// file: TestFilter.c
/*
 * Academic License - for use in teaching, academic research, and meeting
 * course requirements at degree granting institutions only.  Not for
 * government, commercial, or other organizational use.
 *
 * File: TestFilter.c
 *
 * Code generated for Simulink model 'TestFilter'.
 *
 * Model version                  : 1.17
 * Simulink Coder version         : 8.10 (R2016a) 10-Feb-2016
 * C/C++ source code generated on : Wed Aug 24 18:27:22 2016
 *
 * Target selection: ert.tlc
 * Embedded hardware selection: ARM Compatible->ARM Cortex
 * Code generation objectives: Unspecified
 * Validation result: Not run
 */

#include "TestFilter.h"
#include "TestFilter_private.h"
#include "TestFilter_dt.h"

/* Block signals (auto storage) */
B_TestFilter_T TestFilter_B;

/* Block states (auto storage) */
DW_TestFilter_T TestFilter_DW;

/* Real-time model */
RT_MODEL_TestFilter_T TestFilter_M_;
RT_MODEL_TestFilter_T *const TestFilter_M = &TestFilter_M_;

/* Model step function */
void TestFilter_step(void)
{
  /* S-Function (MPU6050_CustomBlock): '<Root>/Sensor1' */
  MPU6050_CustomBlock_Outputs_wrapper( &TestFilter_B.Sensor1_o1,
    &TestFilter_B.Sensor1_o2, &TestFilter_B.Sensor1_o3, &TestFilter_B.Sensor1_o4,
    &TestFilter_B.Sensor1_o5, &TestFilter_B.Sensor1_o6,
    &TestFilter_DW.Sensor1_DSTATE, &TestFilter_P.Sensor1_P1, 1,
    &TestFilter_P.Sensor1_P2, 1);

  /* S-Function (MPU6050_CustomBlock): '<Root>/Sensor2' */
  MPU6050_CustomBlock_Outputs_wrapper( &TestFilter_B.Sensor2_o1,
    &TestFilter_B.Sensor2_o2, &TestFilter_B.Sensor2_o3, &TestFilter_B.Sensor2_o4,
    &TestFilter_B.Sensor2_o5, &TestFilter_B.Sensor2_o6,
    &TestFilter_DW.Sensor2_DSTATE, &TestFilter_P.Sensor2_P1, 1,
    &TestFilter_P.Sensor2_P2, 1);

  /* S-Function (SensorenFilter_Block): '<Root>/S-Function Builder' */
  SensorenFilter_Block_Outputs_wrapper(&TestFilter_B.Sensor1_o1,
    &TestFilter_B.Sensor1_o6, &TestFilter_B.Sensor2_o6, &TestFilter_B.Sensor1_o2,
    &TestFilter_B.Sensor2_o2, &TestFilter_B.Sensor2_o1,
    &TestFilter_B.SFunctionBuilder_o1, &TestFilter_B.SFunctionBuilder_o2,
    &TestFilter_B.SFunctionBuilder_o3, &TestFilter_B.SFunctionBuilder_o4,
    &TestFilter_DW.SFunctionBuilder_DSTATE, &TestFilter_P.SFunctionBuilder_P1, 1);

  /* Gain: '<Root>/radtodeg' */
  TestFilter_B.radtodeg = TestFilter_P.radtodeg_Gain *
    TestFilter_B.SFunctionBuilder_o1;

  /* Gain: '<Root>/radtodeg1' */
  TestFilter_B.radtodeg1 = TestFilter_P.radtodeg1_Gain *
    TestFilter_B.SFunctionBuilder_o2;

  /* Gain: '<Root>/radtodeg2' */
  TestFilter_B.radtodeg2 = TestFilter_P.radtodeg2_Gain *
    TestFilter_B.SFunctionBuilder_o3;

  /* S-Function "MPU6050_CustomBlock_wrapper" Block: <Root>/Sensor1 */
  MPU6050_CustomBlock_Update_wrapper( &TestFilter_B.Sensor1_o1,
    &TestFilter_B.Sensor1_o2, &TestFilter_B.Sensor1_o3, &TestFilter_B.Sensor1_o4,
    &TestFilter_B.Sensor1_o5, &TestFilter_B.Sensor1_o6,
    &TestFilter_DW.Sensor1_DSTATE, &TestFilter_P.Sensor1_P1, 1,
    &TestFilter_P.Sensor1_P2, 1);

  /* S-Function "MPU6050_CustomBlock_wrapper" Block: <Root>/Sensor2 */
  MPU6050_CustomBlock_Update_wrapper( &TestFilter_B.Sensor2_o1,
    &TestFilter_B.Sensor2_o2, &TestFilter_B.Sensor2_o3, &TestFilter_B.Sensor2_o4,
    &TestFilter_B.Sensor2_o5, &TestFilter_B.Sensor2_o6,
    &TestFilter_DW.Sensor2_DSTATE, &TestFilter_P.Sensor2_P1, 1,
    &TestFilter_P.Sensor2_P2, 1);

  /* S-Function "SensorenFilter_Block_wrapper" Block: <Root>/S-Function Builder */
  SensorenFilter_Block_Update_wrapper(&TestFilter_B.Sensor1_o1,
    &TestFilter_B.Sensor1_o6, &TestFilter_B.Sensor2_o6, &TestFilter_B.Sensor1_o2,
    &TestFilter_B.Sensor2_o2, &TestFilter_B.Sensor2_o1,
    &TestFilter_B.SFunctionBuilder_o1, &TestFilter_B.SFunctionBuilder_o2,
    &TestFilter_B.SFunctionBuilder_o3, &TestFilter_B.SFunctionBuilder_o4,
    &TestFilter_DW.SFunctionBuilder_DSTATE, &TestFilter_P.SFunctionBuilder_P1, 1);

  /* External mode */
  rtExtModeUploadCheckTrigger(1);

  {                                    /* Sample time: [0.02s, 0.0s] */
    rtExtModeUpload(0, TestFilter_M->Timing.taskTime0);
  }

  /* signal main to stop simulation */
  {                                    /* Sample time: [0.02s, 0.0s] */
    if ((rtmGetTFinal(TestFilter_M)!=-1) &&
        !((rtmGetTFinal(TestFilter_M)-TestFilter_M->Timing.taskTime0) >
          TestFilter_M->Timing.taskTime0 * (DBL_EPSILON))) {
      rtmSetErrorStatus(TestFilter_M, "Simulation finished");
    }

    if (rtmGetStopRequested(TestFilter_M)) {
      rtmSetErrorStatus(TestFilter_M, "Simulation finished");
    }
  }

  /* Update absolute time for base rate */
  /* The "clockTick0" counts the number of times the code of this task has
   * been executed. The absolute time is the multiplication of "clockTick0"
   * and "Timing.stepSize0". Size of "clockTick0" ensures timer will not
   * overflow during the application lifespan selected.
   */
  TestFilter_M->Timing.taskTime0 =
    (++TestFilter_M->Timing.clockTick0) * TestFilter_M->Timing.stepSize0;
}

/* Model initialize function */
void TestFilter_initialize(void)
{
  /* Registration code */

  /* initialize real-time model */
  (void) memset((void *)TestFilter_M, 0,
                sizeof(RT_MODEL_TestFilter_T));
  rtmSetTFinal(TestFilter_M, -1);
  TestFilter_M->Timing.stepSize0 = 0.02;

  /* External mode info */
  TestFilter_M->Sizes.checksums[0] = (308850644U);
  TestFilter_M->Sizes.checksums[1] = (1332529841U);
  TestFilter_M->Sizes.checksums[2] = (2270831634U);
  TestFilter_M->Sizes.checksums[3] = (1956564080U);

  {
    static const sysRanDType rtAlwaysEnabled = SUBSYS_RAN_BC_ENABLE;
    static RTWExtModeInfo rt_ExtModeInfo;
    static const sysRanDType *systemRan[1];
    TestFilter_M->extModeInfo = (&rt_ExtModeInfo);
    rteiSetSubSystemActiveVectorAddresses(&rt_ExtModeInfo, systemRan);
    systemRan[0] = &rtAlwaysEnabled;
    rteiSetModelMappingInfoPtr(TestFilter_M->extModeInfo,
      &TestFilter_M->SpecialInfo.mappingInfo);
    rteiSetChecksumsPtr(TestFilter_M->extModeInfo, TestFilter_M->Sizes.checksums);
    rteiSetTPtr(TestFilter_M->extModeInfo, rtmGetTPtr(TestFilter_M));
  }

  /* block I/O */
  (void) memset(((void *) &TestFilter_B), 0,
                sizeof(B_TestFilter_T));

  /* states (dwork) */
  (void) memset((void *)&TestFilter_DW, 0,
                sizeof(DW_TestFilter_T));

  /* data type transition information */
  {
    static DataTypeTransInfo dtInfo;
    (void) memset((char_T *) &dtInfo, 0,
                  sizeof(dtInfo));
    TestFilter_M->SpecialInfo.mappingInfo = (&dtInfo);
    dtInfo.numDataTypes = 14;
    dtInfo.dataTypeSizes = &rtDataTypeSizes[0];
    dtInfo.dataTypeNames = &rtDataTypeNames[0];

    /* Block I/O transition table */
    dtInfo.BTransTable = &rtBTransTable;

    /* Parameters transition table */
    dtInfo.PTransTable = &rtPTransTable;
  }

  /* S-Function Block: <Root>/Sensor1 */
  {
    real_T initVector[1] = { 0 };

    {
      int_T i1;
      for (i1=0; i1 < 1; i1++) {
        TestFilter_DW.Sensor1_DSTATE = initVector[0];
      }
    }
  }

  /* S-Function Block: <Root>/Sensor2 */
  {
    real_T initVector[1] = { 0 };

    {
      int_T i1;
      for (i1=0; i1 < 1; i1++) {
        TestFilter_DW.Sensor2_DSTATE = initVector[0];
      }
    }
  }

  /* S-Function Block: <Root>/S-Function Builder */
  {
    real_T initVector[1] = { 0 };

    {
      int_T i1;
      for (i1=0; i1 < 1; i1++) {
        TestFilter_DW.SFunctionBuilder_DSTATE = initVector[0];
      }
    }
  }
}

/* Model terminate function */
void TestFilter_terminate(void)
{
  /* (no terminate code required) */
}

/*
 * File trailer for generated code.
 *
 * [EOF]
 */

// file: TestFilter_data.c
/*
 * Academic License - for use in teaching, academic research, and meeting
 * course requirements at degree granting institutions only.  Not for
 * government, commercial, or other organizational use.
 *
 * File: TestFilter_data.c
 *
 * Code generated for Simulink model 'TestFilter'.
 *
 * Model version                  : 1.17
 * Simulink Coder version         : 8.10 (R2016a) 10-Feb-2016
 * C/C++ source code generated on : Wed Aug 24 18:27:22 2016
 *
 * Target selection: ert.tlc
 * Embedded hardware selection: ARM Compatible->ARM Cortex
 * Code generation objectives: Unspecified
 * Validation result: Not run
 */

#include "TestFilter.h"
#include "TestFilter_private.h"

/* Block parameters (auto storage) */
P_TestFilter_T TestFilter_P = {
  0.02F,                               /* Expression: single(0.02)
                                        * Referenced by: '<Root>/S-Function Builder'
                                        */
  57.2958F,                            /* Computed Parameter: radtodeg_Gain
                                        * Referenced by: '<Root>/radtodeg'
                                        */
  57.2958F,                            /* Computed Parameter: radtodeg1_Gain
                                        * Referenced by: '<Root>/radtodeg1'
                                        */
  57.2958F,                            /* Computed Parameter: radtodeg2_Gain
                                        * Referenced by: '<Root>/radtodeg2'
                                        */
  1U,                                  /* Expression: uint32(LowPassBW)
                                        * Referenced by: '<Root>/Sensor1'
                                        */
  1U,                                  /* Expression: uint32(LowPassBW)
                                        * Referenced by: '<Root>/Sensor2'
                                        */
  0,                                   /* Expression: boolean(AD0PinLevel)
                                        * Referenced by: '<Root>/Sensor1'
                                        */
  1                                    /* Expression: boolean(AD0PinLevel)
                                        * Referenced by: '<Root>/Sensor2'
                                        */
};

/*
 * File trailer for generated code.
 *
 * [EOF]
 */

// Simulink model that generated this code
simulink model "TestFilter"  (R2016a)
settings: Solver=FixedStepDiscrete  StartTime=0.0  StopTime=inf  FixedStep=0.02  RelTol=1e-3

== system TestFilter ==
  S-Function Builder : S-Function  InitFcn=try, set_param(gcb,'FunctionName','SensorenFilter_Block'), end  FunctionName=SensorenFilter_Block  Parameters=single(0.02)  SFunctionModules=SensorenFilter_Block_wrapper  SFunctionDeploymentMode=off  EnableBusSupport=off  mask(S-Function Builder){}
      mask help: Simulink:masks:SFunctionBuilder_MD
      mask init:
      | val = [[.9  0.75 0.75 1 1 .9 .9 1]',[1 1 0.75 0.75 .9 .9 1 .9]'];try , sys = get_param(gcb,'SfunBuilderFcnName');if isempty(sys), sys = get_param(gcb,'FunctionName'); end,catch, sys = get_param(gcb,'FunctionName'); end
  Scope1 : Scope  NumInputPorts=4
  Sensor1 : S-Function  InitFcn=try, set_param(gcb,'FunctionName','MPU6050_CustomBlock'), end  FunctionName=MPU6050_CustomBlock  Parameters=boolean(AD0PinLevel),uint32(LowPassBW)  SFunctionModules=MPU6050_CustomBlock_wrapper  SFunctionDeploymentMode=off  EnableBusSupport=off  mask(S-Function Builder){AD0PinLevel=0, LowPassBW=260}
      mask prompts: AD0PinLevel "Logic-Level of AD0 Pin"; LowPassBW "Low-Pass-Bandwidth [Hz]"
      mask help: Simulink:masks:SFunctionBuilder_MD
      mask init: same as TestFilter/S-Function Builder
  Sensor2 : S-Function  InitFcn=try, set_param(gcb,'FunctionName','MPU6050_CustomBlock'), end  FunctionName=MPU6050_CustomBlock  Parameters=boolean(AD0PinLevel),uint32(LowPassBW)  SFunctionModules=MPU6050_CustomBlock_wrapper  SFunctionDeploymentMode=off  EnableBusSupport=off  mask(S-Function Builder){AD0PinLevel=1, LowPassBW=260}
      mask prompts: AD0PinLevel "Logic-Level of AD0 Pin"; LowPassBW "Low-Pass-Bandwidth [Hz]"
      mask help: Simulink:masks:SFunctionBuilder_MD
      mask init: same as TestFilter/S-Function Builder
  Terminator{,1..5} (6 alike) : Terminator
  radtodeg : Gain  Gain=57.2958
  radtodeg1 : Gain  Gain=57.2958
  radtodeg2 : Gain  Gain=57.2958
  wires:
  Sensor1/3 -> Terminator5/1
  Sensor1/4 -> Terminator4/1
  Sensor1/5 -> Terminator3/1
  Sensor1/1 -> S-Function Builder/1
  Sensor1/2 -> S-Function Builder/4
  Sensor1/6 -> S-Function Builder/2
  Sensor2/1 -> S-Function Builder/6
  Sensor2/2 -> S-Function Builder/5
  Sensor2/6 -> S-Function Builder/3
  Sensor2/5 -> Terminator/1
  Sensor2/4 -> Terminator1/1
  Sensor2/3 -> Terminator2/1
  S-Function Builder/1 -> radtodeg/1
  S-Function Builder/2 -> radtodeg1/1
  S-Function Builder/3 -> radtodeg2/1
  S-Function Builder/4 -> Scope1/4
  radtodeg/1 -> Scope1/1
  radtodeg1/1 -> Scope1/2
  radtodeg2/1 -> Scope1/3
